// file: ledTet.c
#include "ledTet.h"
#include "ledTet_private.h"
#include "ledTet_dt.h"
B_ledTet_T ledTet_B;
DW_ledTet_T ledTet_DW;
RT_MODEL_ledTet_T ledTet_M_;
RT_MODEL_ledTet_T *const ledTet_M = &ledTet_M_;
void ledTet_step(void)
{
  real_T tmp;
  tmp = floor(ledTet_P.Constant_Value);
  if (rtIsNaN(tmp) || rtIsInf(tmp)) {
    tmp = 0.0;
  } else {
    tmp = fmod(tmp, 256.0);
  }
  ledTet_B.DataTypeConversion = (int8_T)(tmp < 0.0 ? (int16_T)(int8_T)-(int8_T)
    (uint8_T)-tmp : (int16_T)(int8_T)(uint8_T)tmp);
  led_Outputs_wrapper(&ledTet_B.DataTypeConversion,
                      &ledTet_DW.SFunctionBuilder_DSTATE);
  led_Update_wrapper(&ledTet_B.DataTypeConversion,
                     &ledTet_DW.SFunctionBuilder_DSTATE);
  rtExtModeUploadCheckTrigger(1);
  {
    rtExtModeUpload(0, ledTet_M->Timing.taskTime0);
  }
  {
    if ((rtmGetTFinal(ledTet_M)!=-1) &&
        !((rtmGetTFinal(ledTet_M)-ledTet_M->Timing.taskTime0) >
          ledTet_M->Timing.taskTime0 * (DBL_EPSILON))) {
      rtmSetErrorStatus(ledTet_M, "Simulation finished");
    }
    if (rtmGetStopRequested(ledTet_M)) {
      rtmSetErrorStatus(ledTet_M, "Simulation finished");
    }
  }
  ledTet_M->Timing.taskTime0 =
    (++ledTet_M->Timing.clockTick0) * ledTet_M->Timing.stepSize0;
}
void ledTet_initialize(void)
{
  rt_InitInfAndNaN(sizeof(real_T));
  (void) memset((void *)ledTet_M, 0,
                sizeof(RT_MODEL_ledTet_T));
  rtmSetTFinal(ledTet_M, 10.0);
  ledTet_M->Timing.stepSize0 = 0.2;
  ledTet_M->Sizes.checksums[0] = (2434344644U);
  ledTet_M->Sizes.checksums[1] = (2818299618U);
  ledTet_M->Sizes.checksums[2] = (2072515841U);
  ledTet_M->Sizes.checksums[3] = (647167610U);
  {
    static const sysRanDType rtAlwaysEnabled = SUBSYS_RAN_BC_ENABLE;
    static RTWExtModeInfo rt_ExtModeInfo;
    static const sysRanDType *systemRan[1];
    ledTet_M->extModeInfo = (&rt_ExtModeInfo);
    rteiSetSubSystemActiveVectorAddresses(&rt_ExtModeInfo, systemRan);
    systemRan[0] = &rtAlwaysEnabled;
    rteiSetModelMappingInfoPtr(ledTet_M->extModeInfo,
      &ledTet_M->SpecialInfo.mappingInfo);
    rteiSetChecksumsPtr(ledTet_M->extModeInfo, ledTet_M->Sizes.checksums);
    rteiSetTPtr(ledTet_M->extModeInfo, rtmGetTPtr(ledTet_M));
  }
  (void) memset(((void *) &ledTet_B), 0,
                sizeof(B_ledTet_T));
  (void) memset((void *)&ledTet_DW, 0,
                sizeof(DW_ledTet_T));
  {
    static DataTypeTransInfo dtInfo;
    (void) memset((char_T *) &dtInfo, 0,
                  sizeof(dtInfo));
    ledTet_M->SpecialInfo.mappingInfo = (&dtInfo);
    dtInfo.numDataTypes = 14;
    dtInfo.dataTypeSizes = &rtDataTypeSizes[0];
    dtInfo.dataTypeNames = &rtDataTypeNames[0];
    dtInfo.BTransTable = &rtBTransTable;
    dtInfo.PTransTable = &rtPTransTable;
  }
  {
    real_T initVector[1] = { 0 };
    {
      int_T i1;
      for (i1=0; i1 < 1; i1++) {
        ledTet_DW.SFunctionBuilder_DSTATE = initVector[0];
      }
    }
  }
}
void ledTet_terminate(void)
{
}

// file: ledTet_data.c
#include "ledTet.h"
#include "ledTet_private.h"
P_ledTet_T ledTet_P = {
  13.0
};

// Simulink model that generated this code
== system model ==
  SFunctionBuilder : S-Function  FunctionName=led  <- 1: DataTypeConversion
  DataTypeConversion : DataTypeConversion  <- 1: Constant
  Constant : Constant  Value=13
